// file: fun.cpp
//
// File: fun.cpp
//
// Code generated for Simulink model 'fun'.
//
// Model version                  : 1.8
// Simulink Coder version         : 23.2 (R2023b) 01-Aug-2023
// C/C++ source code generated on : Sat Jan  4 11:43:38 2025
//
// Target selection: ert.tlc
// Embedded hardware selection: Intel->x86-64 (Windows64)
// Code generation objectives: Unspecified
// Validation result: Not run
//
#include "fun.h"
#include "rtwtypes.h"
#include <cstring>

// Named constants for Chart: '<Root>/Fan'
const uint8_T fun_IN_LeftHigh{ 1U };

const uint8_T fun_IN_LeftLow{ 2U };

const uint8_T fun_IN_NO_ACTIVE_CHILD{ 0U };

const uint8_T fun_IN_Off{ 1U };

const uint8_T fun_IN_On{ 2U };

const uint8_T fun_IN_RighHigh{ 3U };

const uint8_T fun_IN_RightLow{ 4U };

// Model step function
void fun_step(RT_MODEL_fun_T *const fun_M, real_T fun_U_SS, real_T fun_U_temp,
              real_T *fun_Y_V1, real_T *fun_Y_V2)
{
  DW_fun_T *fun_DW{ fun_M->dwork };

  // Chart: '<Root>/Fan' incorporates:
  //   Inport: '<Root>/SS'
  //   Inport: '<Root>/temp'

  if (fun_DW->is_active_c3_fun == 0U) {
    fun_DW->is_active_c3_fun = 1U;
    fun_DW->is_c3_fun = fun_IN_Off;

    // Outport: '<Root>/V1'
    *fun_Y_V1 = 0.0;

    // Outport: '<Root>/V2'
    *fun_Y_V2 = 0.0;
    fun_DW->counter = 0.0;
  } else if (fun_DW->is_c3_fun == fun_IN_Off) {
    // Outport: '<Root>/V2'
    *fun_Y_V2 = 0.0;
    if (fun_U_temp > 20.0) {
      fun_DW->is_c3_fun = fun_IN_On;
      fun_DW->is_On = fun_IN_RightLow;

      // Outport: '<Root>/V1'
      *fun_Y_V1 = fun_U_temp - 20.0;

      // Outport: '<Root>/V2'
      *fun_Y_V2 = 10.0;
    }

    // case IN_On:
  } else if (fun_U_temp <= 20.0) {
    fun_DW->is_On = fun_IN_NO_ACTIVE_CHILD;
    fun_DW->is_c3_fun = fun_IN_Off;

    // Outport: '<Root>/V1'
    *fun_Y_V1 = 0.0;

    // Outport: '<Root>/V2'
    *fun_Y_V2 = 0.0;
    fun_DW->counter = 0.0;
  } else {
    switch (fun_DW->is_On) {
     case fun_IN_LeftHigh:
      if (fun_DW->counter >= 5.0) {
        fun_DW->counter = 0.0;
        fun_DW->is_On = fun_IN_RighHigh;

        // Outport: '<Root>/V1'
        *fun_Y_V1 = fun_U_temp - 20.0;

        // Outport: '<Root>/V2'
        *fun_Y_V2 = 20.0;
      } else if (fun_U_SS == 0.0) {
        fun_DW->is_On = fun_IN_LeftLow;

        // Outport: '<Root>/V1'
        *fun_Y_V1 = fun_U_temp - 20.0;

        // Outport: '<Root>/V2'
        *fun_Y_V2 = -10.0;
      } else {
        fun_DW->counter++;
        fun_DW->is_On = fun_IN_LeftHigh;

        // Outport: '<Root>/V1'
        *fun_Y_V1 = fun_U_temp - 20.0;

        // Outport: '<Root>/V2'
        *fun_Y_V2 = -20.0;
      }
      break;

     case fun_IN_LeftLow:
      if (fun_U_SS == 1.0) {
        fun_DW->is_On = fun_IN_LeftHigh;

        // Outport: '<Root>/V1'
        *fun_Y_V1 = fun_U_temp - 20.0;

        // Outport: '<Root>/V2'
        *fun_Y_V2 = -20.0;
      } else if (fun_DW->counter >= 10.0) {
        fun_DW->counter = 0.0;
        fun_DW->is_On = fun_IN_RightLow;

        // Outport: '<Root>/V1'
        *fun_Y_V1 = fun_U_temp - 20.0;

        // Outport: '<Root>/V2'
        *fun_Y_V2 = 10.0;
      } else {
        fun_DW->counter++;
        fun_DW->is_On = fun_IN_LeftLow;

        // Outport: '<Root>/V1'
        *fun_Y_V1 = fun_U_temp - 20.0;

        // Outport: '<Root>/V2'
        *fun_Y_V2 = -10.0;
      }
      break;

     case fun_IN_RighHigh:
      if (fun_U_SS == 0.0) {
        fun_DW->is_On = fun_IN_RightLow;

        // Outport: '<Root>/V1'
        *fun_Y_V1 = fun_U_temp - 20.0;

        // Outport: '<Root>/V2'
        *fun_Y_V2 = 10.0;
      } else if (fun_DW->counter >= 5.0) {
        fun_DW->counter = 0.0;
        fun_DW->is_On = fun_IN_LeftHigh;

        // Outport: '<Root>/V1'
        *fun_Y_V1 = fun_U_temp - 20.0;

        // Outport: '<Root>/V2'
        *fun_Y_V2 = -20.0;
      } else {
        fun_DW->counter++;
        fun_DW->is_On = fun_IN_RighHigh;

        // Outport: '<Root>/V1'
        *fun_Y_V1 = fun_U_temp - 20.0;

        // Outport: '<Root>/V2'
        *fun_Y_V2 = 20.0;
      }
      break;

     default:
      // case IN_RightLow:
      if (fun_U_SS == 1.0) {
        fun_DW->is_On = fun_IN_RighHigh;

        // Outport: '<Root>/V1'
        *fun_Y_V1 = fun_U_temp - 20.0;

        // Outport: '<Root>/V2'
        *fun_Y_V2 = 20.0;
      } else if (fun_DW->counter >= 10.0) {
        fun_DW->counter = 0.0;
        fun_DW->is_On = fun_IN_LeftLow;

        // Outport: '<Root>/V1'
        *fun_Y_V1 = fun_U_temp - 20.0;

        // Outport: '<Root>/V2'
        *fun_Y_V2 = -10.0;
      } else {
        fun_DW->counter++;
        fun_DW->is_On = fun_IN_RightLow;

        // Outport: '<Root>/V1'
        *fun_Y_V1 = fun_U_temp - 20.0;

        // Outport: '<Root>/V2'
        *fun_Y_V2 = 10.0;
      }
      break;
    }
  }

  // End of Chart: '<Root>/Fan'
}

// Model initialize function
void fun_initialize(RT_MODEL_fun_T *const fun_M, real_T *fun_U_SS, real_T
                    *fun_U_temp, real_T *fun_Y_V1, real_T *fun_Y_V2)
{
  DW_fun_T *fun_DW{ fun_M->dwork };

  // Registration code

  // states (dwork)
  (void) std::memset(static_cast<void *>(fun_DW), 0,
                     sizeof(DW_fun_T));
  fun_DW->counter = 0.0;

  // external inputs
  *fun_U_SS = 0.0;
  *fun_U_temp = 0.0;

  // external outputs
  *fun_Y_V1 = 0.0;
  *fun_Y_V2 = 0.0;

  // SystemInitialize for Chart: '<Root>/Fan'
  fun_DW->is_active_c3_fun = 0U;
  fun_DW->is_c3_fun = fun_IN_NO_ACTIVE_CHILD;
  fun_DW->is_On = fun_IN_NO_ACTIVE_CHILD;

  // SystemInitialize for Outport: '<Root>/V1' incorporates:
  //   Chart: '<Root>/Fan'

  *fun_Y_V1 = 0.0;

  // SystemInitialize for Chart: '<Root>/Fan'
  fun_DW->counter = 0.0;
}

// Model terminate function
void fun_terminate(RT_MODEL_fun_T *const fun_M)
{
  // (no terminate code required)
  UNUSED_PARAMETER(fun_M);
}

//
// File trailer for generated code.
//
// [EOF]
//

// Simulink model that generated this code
simulink model "fun"  (R2023b)
settings: Solver=FixedStepAuto  StartTime=0.0  StopTime=10  FixedStep=1  RelTol=1e-3

== system fun ==
  SS : Inport  OutDataTypeStr=fixdt(1,16,4)
  temp : Inport  Port=2  OutDataTypeStr=fixdt(1,16,4)
  Fan : Stateflow chart  TreatAsAtomicUnit=on
  Fan_boundary_DTC : DataTypeConversion
  Fan_boundary_DTC1 : DataTypeConversion
  V1_boundary_DTC : DataTypeConversion
  V2_boundary_DTC : DataTypeConversion
  V1 : Outport
  V2 : Outport  Port=2
  wires:
  SS/1 -> Fan_boundary_DTC/1
  Fan_boundary_DTC/1 -> Fan/1(SS)
  temp/1 -> Fan_boundary_DTC1/1
  Fan_boundary_DTC1/1 -> Fan/2(temp)
  Fan/1(V1) -> V1_boundary_DTC/1
  V1_boundary_DTC/1 -> V1/1
  Fan/2(V2) -> V2_boundary_DTC/1
  V2_boundary_DTC/1 -> V2/1

== stateflow chart fun/Fan ==
  state On
    state RightLow
      entry:
      V1  = temp - 20;
      V2 = 10;
    state RighHigh
      entry:
      V1  = temp - 20;
      V2 = 20;
    state LeftLow
      entry:
      V1  = temp - 20;
      V2 = -10;
    state LeftHigh
      entry:
      V1  = temp - 20;
      V2 = -20;
    (default) -> RightLow
    RighHigh -> RighHigh [order 3] : {counter = counter + 1;}
    RightLow -> RighHigh [order 1] : [SS == 1]
    RightLow -> RightLow [order 3] : {counter = counter +1}
    RighHigh -> RightLow [order 1] : [SS == 0]
    RightLow -> LeftLow [order 2] : [counter >= 10]{counter = 0}
    LeftLow -> RightLow [order 2] : [counter >= 10]{counter = 0}
    LeftHigh -> RighHigh [order 1] : [counter >= 5]{counter = 0}
    RighHigh -> LeftHigh [order 2] : [counter >= 5]{counter = 0}
    LeftLow -> LeftHigh [order 1] : [SS == 1]
    LeftLow -> LeftLow [order 3] : {counter = counter + 1}
    LeftHigh -> LeftHigh [order 3] : {counter = counter +1}
    LeftHigh -> LeftLow [order 2] : [SS == 0]
  state Off
    entry:
    V1 = 0;
    V2 = 0;
    counter = 0;
  (default) -> Off
  Off -> On : [temp > 20]
  On -> Off : [temp <= 20]
  data: V1 output fixdt(1,16,0); V2 output fixdt(1,16,0); SS input fixdt(1,16,0); counter local fixdt(1,16,0); temp input fixdt(1,16,0)
